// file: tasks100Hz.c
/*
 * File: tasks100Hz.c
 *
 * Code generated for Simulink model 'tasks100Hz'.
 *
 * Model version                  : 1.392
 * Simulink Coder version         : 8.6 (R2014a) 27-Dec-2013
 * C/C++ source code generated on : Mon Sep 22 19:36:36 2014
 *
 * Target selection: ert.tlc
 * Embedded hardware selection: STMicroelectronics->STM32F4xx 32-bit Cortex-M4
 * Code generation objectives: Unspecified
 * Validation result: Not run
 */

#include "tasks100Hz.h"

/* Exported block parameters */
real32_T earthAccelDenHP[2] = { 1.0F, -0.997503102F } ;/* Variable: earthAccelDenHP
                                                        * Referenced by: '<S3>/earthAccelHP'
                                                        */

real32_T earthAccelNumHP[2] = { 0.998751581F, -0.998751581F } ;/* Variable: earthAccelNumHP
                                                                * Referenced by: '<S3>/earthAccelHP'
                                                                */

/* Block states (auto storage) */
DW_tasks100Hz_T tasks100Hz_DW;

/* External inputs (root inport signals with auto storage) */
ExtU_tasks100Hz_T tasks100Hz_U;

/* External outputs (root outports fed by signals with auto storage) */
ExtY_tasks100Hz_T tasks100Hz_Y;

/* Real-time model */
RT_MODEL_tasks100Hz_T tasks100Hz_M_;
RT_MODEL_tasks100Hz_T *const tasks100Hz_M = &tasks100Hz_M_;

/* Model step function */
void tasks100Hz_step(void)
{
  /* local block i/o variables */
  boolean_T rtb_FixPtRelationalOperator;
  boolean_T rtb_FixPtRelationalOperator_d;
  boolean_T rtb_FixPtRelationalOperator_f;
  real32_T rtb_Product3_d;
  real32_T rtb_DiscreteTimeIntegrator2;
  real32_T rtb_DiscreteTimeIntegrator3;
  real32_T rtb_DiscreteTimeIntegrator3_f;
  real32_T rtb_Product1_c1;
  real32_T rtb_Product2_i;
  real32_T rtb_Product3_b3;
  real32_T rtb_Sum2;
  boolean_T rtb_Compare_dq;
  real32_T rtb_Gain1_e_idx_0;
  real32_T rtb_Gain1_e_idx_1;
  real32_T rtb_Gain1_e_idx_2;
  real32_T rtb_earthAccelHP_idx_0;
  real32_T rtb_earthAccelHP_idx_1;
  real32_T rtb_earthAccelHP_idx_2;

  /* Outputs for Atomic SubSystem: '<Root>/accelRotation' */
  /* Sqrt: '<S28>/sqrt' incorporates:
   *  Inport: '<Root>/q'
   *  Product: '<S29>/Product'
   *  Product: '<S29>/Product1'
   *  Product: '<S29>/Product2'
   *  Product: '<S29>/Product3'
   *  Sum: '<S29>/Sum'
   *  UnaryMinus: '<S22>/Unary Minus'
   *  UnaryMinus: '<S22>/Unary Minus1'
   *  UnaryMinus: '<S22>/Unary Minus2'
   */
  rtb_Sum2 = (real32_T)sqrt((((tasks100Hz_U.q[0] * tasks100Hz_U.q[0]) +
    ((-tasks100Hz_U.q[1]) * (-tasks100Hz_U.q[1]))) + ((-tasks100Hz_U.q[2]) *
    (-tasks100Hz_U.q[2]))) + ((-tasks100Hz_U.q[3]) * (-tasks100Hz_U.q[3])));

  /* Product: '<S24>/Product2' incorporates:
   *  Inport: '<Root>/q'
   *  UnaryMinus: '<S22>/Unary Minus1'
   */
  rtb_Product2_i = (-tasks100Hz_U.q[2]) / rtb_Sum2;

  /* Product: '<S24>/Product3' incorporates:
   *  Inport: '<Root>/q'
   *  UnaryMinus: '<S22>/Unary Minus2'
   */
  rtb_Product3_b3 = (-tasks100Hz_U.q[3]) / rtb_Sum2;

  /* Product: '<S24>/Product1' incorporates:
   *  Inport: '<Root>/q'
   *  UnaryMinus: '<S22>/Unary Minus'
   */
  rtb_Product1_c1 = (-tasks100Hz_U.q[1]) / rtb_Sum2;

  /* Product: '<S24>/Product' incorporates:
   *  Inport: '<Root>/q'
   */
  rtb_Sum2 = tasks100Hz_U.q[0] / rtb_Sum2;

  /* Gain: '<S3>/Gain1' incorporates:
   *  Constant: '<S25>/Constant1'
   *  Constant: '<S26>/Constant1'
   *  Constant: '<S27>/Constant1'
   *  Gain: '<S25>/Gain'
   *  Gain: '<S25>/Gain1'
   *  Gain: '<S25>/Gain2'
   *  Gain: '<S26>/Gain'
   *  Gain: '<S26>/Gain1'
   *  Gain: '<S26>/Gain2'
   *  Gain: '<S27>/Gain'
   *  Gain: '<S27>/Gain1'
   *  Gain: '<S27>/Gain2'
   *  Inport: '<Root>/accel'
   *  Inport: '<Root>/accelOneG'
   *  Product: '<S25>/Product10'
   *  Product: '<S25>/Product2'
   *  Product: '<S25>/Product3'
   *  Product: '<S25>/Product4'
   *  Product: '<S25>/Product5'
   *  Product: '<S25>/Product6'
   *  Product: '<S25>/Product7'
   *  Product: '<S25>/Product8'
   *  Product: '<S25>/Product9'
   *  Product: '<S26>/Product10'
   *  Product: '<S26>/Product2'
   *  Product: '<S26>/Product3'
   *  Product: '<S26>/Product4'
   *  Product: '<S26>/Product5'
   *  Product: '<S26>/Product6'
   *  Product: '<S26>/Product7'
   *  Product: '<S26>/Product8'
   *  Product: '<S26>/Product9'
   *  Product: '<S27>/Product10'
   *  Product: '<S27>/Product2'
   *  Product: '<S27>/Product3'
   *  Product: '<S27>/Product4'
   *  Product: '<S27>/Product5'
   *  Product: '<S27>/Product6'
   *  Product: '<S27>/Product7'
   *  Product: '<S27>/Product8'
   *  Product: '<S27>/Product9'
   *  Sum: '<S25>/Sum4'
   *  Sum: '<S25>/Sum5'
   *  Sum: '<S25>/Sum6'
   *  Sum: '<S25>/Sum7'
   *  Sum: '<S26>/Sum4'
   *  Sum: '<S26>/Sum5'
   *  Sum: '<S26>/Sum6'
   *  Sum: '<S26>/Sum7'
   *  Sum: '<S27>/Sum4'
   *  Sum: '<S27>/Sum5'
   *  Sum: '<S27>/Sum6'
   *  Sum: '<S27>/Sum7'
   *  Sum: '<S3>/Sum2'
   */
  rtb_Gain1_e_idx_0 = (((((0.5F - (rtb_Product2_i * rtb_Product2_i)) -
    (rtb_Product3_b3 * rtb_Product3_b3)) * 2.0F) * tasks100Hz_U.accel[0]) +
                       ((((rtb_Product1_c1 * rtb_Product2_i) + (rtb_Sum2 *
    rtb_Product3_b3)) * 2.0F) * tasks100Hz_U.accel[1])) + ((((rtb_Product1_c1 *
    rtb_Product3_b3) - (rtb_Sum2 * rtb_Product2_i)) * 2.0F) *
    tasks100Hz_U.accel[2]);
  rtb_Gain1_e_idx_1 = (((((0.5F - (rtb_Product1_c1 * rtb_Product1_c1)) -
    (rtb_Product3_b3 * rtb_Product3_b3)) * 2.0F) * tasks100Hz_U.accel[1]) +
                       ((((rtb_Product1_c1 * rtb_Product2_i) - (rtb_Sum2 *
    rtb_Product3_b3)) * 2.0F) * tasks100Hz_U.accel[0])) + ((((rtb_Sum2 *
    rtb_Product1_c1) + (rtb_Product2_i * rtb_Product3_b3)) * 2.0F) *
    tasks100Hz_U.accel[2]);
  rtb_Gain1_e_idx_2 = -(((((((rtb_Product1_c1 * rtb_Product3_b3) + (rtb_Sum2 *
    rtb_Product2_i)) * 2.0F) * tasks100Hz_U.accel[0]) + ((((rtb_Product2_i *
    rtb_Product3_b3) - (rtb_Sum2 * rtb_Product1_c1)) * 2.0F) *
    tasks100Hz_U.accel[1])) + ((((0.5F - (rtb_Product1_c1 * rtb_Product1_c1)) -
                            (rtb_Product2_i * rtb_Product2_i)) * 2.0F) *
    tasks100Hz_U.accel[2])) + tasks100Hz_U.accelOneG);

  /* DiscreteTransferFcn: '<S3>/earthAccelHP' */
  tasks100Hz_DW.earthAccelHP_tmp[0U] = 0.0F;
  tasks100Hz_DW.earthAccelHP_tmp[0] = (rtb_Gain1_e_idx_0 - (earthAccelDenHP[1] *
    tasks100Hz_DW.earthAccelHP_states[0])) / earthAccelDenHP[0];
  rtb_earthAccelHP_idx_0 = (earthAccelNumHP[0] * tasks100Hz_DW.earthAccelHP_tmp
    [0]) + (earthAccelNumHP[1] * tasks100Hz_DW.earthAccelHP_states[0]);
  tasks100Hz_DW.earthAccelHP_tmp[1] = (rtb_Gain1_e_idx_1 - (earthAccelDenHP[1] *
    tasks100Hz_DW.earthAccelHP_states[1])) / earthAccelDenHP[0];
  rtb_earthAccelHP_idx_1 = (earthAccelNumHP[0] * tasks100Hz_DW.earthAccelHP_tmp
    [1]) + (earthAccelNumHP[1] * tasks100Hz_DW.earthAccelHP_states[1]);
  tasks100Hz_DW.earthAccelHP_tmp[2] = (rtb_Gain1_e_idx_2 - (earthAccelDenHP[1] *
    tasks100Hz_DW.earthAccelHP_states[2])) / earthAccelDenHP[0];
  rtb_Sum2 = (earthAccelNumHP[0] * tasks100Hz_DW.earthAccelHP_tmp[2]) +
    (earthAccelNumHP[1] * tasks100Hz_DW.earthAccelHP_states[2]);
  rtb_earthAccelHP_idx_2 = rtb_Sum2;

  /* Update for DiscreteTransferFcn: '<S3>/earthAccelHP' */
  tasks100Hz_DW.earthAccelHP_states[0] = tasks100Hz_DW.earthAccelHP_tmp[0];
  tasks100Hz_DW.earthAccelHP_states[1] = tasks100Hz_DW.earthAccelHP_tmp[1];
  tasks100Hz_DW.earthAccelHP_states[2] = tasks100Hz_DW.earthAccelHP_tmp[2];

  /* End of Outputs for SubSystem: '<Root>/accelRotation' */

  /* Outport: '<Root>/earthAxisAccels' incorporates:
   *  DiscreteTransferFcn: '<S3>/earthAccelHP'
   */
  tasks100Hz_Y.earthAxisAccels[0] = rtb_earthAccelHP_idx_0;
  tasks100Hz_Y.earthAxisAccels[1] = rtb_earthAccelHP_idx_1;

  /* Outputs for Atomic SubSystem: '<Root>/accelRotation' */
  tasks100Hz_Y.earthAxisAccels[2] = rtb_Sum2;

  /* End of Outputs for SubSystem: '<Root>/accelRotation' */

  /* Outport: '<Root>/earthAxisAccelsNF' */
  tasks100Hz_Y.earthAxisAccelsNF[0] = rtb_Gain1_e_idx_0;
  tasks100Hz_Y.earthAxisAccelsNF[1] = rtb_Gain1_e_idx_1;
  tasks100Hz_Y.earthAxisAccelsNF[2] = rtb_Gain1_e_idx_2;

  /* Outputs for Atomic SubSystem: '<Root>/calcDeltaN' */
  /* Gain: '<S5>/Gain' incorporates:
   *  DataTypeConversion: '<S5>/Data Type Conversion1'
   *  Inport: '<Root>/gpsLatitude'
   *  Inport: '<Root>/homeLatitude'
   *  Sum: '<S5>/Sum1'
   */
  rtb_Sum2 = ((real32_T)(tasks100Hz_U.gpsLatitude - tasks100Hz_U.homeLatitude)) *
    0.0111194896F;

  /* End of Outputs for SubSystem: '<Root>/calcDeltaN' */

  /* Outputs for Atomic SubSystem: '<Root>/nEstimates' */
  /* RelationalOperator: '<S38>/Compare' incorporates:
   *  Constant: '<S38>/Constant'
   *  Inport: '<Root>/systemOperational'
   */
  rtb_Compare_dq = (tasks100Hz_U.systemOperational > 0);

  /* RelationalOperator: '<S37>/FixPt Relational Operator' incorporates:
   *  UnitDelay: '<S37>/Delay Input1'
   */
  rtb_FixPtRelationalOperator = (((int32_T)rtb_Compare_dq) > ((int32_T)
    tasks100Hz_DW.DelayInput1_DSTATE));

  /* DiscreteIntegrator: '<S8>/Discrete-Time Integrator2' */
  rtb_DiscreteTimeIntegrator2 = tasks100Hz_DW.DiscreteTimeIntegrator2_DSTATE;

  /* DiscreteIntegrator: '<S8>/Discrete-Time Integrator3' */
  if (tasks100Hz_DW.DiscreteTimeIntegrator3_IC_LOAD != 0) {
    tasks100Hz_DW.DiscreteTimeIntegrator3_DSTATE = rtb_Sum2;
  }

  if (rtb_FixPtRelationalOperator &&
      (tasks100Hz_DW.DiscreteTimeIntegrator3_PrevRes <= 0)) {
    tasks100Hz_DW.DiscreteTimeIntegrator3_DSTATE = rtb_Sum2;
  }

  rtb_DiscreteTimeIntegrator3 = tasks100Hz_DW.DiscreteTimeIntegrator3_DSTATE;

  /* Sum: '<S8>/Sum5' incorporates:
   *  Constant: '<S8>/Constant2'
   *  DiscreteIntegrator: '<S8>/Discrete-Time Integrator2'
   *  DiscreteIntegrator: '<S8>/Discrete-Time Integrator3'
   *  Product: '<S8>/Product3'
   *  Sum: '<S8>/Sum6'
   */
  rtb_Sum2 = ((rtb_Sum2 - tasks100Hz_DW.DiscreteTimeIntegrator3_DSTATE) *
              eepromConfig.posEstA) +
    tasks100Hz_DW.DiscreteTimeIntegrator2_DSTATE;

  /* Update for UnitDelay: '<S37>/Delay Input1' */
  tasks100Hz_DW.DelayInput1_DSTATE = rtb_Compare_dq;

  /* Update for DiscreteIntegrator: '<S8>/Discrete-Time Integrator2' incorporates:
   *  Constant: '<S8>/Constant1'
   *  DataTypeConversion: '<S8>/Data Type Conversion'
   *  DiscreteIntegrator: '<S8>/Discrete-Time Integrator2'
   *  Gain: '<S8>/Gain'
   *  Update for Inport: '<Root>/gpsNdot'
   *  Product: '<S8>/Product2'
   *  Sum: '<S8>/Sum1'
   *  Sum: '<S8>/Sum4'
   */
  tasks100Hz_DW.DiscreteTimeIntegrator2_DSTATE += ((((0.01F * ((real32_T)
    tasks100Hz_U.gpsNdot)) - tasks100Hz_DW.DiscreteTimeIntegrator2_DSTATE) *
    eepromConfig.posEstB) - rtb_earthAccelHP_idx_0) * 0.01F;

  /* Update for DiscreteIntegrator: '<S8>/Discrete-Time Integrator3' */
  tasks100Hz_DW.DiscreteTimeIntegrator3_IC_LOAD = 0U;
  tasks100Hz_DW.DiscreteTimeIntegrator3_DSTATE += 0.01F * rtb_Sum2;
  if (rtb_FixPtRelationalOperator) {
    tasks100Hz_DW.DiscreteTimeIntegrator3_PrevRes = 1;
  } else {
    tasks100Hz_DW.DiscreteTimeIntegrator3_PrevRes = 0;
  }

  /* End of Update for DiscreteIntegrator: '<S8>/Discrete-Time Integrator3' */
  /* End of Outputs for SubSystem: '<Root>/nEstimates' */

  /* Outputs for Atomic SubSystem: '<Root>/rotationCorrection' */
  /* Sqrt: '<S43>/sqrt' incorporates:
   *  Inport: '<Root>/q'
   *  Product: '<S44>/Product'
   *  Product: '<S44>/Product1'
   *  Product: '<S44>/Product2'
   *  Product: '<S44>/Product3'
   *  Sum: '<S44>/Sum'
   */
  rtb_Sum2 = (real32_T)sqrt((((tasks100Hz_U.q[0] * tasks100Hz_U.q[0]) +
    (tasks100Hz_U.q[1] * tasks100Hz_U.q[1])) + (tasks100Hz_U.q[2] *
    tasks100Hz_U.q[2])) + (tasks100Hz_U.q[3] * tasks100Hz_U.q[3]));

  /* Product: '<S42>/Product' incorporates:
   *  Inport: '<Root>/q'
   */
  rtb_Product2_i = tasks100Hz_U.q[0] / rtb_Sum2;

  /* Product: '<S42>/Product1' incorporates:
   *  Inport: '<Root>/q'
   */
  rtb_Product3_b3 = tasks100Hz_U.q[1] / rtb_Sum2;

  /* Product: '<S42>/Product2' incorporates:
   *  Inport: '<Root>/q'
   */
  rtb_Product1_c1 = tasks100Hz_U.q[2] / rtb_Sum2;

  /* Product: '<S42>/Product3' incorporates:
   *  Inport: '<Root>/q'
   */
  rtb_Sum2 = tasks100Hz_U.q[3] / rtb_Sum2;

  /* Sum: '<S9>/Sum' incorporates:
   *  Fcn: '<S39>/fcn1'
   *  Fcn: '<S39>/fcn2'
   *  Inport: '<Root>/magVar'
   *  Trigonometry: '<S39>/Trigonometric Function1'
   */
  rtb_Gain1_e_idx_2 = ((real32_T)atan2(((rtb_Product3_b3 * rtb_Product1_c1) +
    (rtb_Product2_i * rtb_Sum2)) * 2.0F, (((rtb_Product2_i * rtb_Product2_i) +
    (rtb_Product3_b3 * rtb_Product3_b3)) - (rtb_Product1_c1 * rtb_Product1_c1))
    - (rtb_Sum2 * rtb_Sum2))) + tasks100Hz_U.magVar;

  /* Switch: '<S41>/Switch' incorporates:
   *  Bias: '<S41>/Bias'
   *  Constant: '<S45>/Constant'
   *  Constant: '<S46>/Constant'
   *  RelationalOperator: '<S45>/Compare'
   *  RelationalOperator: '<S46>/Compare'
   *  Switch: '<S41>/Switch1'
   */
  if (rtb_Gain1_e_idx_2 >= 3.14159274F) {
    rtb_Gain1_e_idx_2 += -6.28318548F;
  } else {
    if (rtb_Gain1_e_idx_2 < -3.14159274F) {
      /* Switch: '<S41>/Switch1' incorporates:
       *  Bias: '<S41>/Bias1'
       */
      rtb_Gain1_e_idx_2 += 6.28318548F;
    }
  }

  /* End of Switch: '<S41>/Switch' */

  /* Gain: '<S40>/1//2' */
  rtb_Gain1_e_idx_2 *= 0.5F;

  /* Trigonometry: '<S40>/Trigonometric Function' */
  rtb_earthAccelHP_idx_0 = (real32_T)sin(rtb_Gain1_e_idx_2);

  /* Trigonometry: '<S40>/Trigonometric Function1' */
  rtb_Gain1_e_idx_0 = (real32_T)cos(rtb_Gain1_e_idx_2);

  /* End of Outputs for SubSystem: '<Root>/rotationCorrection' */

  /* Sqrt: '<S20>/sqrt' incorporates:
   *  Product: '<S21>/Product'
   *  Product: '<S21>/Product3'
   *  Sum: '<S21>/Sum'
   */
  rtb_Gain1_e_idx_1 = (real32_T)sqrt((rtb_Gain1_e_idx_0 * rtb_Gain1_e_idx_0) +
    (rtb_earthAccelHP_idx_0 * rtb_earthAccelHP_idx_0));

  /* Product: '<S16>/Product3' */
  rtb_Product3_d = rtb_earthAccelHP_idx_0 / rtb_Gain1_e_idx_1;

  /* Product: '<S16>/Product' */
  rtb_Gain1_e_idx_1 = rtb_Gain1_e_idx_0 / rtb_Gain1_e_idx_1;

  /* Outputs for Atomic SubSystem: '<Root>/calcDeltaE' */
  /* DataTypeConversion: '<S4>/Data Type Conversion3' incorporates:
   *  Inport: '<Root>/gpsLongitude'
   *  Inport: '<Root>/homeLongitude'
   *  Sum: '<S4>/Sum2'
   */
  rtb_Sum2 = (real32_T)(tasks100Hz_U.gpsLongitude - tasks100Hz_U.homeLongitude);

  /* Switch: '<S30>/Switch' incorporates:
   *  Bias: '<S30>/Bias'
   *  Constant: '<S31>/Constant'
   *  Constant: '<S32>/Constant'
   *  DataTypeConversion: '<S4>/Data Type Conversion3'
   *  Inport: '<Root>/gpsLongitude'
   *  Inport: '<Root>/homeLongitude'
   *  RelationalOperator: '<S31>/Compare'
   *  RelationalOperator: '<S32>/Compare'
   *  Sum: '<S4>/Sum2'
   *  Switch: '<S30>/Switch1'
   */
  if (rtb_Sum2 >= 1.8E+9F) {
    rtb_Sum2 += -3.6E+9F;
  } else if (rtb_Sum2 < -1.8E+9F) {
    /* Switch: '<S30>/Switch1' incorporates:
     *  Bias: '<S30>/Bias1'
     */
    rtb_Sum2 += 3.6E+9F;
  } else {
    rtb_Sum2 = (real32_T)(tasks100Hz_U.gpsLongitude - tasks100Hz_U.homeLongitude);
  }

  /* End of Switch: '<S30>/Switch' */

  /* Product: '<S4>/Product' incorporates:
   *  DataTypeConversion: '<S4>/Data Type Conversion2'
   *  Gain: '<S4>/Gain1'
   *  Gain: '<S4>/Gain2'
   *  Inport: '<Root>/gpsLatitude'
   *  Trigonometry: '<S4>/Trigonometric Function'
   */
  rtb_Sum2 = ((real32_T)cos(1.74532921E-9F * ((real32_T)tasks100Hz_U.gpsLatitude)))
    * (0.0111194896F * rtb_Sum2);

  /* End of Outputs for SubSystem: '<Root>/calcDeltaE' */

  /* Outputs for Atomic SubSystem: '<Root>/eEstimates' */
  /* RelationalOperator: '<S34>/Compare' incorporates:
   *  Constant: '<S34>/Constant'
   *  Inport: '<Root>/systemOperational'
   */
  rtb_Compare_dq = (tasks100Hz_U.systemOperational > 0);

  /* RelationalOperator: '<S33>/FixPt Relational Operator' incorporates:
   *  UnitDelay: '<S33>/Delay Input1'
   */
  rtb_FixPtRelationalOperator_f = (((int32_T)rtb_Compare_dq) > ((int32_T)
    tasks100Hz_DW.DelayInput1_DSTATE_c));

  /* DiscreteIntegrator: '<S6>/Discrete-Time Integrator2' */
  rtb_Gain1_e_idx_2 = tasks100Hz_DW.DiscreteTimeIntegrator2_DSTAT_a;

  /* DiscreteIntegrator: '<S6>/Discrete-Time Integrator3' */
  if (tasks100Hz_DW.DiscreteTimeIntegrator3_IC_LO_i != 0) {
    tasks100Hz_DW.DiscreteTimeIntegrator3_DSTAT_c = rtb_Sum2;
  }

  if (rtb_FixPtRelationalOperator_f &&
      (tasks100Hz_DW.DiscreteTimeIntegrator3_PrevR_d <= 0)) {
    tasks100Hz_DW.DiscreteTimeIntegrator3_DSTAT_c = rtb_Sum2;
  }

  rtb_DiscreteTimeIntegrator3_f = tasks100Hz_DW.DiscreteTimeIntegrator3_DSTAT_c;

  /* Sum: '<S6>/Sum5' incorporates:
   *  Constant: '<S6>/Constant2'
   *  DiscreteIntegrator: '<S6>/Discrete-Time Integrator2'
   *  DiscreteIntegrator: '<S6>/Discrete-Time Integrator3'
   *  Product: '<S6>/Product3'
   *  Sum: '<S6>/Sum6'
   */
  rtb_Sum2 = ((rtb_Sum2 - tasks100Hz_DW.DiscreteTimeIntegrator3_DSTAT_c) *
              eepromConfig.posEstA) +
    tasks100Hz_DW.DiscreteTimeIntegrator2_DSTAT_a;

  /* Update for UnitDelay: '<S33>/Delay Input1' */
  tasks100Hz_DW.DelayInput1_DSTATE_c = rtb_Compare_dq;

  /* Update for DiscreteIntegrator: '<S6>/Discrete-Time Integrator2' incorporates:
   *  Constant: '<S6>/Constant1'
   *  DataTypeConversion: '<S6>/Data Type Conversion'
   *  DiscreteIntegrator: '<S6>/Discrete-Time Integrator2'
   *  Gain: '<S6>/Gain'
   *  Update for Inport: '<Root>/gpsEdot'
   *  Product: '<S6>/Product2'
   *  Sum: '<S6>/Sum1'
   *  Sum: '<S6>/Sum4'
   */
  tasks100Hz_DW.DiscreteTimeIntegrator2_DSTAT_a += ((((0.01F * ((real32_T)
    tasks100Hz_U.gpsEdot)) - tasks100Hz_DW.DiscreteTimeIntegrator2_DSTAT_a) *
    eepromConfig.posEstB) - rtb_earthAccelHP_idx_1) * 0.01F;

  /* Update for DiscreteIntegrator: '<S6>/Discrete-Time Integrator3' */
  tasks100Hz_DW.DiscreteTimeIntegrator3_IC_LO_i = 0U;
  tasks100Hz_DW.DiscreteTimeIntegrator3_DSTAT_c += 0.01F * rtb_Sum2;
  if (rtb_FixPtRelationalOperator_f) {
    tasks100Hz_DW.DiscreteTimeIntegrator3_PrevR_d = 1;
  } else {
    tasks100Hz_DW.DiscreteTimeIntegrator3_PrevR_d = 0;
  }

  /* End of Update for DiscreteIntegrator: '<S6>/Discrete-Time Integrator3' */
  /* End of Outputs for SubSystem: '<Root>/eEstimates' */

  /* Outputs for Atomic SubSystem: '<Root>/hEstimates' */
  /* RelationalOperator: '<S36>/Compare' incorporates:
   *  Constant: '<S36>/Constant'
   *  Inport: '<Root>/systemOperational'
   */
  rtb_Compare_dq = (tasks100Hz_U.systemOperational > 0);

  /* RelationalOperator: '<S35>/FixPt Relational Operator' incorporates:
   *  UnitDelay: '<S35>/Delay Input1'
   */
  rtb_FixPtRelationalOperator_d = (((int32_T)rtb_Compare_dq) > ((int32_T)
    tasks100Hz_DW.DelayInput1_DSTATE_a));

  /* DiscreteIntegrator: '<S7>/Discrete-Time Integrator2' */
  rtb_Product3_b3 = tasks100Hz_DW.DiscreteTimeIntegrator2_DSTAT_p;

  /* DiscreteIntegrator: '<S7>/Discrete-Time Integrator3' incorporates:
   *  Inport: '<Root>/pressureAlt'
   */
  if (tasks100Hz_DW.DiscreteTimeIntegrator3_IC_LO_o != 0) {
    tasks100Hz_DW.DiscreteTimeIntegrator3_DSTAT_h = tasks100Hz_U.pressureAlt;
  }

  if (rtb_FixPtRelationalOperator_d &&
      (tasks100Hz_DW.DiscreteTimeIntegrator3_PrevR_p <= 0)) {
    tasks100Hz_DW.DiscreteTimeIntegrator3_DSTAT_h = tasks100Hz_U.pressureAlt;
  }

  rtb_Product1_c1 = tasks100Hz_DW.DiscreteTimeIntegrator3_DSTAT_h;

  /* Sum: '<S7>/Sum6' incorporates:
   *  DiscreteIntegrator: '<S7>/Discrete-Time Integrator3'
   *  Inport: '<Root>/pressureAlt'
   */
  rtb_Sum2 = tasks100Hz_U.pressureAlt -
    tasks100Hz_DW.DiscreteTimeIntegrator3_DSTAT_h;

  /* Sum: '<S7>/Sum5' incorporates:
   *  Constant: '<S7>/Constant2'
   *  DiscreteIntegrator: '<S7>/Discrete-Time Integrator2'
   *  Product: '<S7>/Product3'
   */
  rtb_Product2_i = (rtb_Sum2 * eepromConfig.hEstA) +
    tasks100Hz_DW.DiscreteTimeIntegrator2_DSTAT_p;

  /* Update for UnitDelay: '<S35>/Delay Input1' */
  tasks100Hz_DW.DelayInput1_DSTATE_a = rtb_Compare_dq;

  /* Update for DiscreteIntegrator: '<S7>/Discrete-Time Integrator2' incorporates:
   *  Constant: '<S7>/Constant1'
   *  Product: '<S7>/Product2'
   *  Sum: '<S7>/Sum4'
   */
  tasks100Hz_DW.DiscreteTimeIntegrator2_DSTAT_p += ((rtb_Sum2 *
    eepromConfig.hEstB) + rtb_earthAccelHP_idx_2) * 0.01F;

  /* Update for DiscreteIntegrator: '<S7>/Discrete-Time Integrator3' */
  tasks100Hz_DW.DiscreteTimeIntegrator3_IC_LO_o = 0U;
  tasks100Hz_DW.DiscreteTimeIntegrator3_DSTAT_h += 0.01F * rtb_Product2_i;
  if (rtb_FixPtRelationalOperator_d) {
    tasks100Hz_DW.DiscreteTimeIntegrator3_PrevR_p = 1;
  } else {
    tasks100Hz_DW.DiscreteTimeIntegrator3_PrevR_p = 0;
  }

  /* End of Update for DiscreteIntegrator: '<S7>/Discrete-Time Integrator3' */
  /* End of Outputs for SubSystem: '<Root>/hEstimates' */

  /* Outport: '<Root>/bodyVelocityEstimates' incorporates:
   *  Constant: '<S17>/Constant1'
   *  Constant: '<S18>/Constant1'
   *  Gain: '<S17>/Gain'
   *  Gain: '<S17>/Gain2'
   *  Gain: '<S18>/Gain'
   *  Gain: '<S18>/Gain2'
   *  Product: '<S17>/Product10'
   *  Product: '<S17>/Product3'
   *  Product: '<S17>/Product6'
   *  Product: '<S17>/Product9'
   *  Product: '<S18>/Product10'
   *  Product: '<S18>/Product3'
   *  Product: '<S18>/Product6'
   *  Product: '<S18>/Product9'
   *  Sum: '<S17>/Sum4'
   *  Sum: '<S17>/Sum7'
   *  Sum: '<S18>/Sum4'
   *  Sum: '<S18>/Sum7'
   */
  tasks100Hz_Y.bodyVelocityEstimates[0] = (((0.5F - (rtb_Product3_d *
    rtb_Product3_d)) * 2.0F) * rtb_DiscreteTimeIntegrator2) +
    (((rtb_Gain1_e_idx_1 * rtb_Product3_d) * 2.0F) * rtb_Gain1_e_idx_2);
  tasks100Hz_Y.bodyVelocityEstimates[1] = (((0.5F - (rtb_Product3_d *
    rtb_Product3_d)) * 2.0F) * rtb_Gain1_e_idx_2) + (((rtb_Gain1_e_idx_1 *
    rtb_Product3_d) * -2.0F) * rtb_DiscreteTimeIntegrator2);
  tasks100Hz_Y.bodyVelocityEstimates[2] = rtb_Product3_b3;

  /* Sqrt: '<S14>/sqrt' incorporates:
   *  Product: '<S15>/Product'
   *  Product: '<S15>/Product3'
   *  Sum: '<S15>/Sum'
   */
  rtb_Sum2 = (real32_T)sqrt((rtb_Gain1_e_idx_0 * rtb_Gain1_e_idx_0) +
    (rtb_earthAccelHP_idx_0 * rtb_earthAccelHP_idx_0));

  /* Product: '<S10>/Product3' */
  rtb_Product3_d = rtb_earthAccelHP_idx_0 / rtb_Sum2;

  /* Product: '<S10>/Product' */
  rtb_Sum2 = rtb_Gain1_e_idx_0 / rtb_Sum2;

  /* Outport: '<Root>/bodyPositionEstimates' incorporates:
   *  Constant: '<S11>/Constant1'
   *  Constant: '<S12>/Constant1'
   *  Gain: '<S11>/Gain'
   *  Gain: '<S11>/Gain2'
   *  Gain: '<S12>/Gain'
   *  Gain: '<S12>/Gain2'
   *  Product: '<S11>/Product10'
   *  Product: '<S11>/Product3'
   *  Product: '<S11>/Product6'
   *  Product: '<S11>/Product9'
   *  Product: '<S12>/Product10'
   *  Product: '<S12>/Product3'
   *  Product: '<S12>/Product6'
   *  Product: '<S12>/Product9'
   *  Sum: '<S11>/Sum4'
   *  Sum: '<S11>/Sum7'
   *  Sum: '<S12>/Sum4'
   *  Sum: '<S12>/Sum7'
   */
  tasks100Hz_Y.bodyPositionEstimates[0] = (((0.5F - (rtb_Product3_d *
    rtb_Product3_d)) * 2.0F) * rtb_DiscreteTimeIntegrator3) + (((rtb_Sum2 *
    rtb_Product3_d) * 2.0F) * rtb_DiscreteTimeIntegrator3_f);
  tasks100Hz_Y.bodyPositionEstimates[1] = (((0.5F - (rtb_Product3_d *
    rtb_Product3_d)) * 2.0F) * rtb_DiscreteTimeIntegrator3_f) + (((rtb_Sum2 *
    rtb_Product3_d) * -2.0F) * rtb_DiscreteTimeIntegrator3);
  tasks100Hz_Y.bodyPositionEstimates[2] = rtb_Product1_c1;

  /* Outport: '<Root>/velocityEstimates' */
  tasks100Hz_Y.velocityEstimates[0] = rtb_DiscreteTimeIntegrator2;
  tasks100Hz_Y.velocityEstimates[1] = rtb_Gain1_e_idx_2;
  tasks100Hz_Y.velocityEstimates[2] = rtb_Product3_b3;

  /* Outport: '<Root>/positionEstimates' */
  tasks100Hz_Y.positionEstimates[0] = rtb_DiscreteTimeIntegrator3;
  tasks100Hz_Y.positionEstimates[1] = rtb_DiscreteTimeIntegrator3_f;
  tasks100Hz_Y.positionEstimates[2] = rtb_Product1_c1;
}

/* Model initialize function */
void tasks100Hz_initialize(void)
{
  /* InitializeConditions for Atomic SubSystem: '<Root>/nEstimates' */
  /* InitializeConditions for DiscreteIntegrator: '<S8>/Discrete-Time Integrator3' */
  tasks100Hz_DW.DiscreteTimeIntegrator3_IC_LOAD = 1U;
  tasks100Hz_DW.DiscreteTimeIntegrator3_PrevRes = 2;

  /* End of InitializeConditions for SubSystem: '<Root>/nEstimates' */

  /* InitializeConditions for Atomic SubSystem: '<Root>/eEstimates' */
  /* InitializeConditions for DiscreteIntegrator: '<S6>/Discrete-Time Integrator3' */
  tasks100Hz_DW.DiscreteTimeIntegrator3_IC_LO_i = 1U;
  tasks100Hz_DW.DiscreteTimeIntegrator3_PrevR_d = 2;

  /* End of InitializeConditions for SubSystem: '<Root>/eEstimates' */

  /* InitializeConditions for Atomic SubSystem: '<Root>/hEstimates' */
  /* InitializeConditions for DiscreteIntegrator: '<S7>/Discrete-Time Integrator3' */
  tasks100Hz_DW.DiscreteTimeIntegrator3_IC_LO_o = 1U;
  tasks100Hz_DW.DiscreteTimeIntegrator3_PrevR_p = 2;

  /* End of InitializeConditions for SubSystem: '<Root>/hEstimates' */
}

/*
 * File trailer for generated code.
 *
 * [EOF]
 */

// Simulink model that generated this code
simulink model "tasks100Hz"  (R2014a)
settings: Solver=FixedStepDiscrete  StartTime=0.0  StopTime=simTime  FixedStep=filterDT  RelTol=1e-3
values from neighbouring files (symbols this model uses):
  earthAccelDenHP = p    [setup.m]
  earthAccelNumHP = p    [setup.m]
  eepromConfig = p    [setup.m]
  filterDT = 1 / 100    (= 0.01)    [setup.m]
undefined symbols (not defined in the file or in its folder): DiscIntNeverNeededParam
libraries: simulink x7, aerolibutil x4, aerolibtransform2 x1

== system tasks100Hz ==
  q : Inport  OutDataTypeStr=single  PortDimensions=4  SampleTime=filterDT
  accel : Inport  Port=2  OutDataTypeStr=single  PortDimensions=3  SampleTime=filterDT
  accelOneG : Inport  Port=3  OutDataTypeStr=single  PortDimensions=1  SampleTime=filterDT
  gpsLatitude : Inport  Port=4  OutDataTypeStr=int32  PortDimensions=1  SampleTime=filterDT
  homeLatitude : Inport  Port=5  OutDataTypeStr=int32  PortDimensions=1  SampleTime=filterDT
  gpsNdot : Inport  Port=6  OutDataTypeStr=int32  PortDimensions=1  SampleTime=filterDT
  gpsLongitude : Inport  Port=7  OutDataTypeStr=int32  PortDimensions=1  SampleTime=filterDT
  homeLongitude : Inport  Port=8  OutDataTypeStr=int32  PortDimensions=1  SampleTime=filterDT
  gpsEdot : Inport  Port=9  OutDataTypeStr=int32  PortDimensions=1  SampleTime=filterDT
  pressureAlt : Inport  Port=10  OutDataTypeStr=single  PortDimensions=1  SampleTime=filterDT
  systemOperational : Inport  Port=11  OutDataTypeStr=uint8  PortDimensions=1  SampleTime=filterDT
  magVar : Inport  Port=12  OutDataTypeStr=single  PortDimensions=1  SampleTime=filterDT
  Data Type Conversion4 : DataTypeConversion  OutDataTypeStr=single
  Data Type Conversion5 : DataTypeConversion  OutDataTypeStr=single
  Mux : Mux  Inputs=3
  Mux2 : Mux  Inputs=3
  Quaternion Rotation1 : Subsystem
  Quaternion Rotation2 : Subsystem
  accelRotation : Subsystem  TreatAsAtomicUnit=on
  calcDeltaE : Subsystem  TreatAsAtomicUnit=on
  calcDeltaN : Subsystem  TreatAsAtomicUnit=on
  eEstimates : Subsystem  TreatAsAtomicUnit=on
  hEstimates : Subsystem  TreatAsAtomicUnit=on
  nEstimates : Subsystem  TreatAsAtomicUnit=on
  rotationCorrection : Subsystem  TreatAsAtomicUnit=on
  earthAxisAccels : Outport  OutDataTypeStr=single  PortDimensions=3  SampleTime=filterDT
  earthAxisAccelsNF : Outport  Port=2  OutDataTypeStr=single  PortDimensions=3  SampleTime=filterDT
  bodyVelocityEstimates : Outport  Port=3  OutDataTypeStr=single  PortDimensions=3  SampleTime=filterDT
  bodyPositionEstimates : Outport  Port=4  OutDataTypeStr=single  PortDimensions=3  SampleTime=filterDT
  velocityEstimates : Outport  Port=5  OutDataTypeStr=single  PortDimensions=3  SampleTime=filterDT
  positionEstimates : Outport  Port=6  OutDataTypeStr=single  PortDimensions=3  SampleTime=filterDT
  wires:
  systemOperational/1 -> nEstimates/2(systemOperational), eEstimates/2(systemOperational), hEstimates/2(systemOperational)
  pressureAlt/1 -> hEstimates/3(pressureAlt)
  hEstimates/1(hDotEstimate) -> Mux/3
  gpsNdot/1 -> nEstimates/4(nDotGPS)
  gpsEdot/1 -> eEstimates/4(eDotGPS)
  nEstimates/1(nDotEstimate) -> Mux/1
  nEstimates/2(nEstimate) -> Mux2/1
  eEstimates/1(eDotEstimate) -> Mux/2
  eEstimates/2(eEstimate) -> Mux2/2
  Quaternion Rotation2/1(vec_rot) -> Data Type Conversion4/1
  Quaternion Rotation1/1(vec_rot) -> Data Type Conversion5/1
  Data Type Conversion4/1 -> bodyVelocityEstimates/1
  Data Type Conversion5/1 -> bodyPositionEstimates/1
  hEstimates/2(hEstimate) -> Mux2/3
  Mux2/1 -> positionEstimates/1, Quaternion Rotation1/2(vec)
  accelOneG/1 -> accelRotation/3(accelOneG)
  homeLatitude/1 -> calcDeltaN/2(homeLatitude)
  calcDeltaN/1(deltaN) -> nEstimates/3(deltaN)
  gpsLongitude/1 -> calcDeltaE/2(gpsLongitude)
  homeLongitude/1 -> calcDeltaE/3(homeLongitude)
  calcDeltaE/1(deltaE) -> eEstimates/3(deltaE)
  gpsLatitude/1 -> calcDeltaN/1(gpsLatitude), calcDeltaE/1(gpsLatitude)
  q/1 -> rotationCorrection/2(qIn), accelRotation/1(q)
  accelRotation/2(earthAxisAccelsNF) -> earthAxisAccelsNF/1
  accelRotation/1(earthAxisAccels) -> eEstimates/1(earthAxisAccels), hEstimates/1(earthAxisAccels), nEstimates/1(earthAxisAccels), earthAxisAccels/1
  accel/1 -> accelRotation/2(accel)
  Mux/1 -> velocityEstimates/1, Quaternion Rotation2/2(vec)
  magVar/1 -> rotationCorrection/1(magVar)
  rotationCorrection/1(qOut) -> Quaternion Rotation2/1(q), Quaternion Rotation1/1(q)

== system tasks100Hz/Quaternion Rotation1 ==
  q : Inport
  vec : Inport  Port=2
  Mux1 : Mux  Inputs=3
  Quaternion Normalize : aerolibutil/Quaternion Normalize
  singleV1 : Subsystem
  singleV2 : Subsystem
  singleV3 : Subsystem
  vec_rot : Outport
  wires:
  q/1 -> Quaternion Normalize/1
  singleV1/1(V1) -> Mux1/1
  vec/1 -> singleV1/2(vec), singleV3/2(vec), singleV2/2(vec)
  Quaternion Normalize/1 -> singleV1/1(q), singleV3/1(q), singleV2/1(q)
  Mux1/1 -> vec_rot/1
  singleV3/1(V3) -> Mux1/3
  singleV2/1(V2) -> Mux1/2

== system tasks100Hz/Quaternion Rotation2 ==
  q : Inport
  vec : Inport  Port=2
  Mux1 : Mux  Inputs=3
  Quaternion Normalize : aerolibutil/Quaternion Normalize
  singleV1 : Subsystem
  singleV2 : Subsystem
  singleV3 : Subsystem
  vec_rot : Outport
  wires:
  singleV2/1(V2) -> Mux1/2
  singleV3/1(V3) -> Mux1/3
  Mux1/1 -> vec_rot/1
  Quaternion Normalize/1 -> singleV2/1(q), singleV3/1(q), singleV1/1(q)
  vec/1 -> singleV2/2(vec), singleV3/2(vec), singleV1/2(vec)
  singleV1/1(V1) -> Mux1/1
  q/1 -> Quaternion Normalize/1

== system tasks100Hz/accelRotation ==
  q : Inport
  accel : Inport  Port=2
  accelOneG : Inport  Port=3
  Demux1 : Demux  Outputs=[2 1]
  Gain1 : Gain  Gain=[1 1 -1]
  Mux1 : Mux  Inputs=[2 1]
  Quaternion Conjugate : aerolibutil/Quaternion Conjugate
  Quaternion Rotation : Subsystem
  Sum2 : Sum  Inputs=|++
  earthAccelHP : DiscreteTransferFcn  Numerator=earthAccelNumHP  Denominator=earthAccelDenHP
  earthAxisAccels : Outport
  earthAxisAccelsNF : Outport  Port=2
  wires:
  Gain1/1 -> earthAxisAccelsNF/1, earthAccelHP/1
  accelOneG/1 -> Sum2/2
  Demux1/1 -> Mux1/1
  Sum2/1 -> Mux1/2
  Demux1/2 -> Sum2/1
  Quaternion Conjugate/1 -> Quaternion Rotation/1(q)
  accel/1 -> Quaternion Rotation/2(vec)
  q/1 -> Quaternion Conjugate/1
  Quaternion Rotation/1(vec_rot) -> Demux1/1
  Mux1/1 -> Gain1/1
  earthAccelHP/1 -> earthAxisAccels/1

== system tasks100Hz/calcDeltaE ==
  gpsLatitude : Inport
  gpsLongitude : Inport  Port=2
  homeLongitude : Inport  Port=3
  Data Type Conversion2 : DataTypeConversion  OutDataTypeStr=single
  Data Type Conversion3 : DataTypeConversion  OutDataTypeStr=single
  Gain1 : Gain  Gain=pi / 180 * 1e-7
  Gain2 : Gain  Gain=0.01111949
  Product : Product
  Sum2 : Sum  Inputs=|+-
  Trigonometric Function : Trigonometry  Operator=cos
  stdRadianLimit : Subsystem
  deltaE : Outport
  wires:
  stdRadianLimit/1(stdDegrees) -> Gain2/1
  gpsLatitude/1 -> Data Type Conversion2/1
  Data Type Conversion3/1 -> stdRadianLimit/1(degrees)
  Product/1 -> deltaE/1
  Sum2/1 -> Data Type Conversion3/1
  homeLongitude/1 -> Sum2/2
  Gain2/1 -> Product/2
  Trigonometric Function/1 -> Product/1
  Gain1/1 -> Trigonometric Function/1
  Data Type Conversion2/1 -> Gain1/1
  gpsLongitude/1 -> Sum2/1

== system tasks100Hz/calcDeltaN ==
  gpsLatitude : Inport
  homeLatitude : Inport  Port=2
  Data Type Conversion1 : DataTypeConversion  OutDataTypeStr=single
  Gain : Gain  Gain=0.01111949
  Sum1 : Sum  Inputs=|+-
  deltaN : Outport
  wires:
  Sum1/1 -> Data Type Conversion1/1
  homeLatitude/1 -> Sum1/2
  Data Type Conversion1/1 -> Gain/1
  gpsLatitude/1 -> Sum1/1
  Gain/1 -> deltaN/1

== system tasks100Hz/eEstimates ==
  earthAxisAccels : Inport
  systemOperational : Inport  Port=2
  deltaE : Inport  Port=3
  eDotGPS : Inport  Port=4  OutDataTypeStr=int32
  Constant1 : Constant  Value=eepromConfig.posEstB  SampleTime=filterDT
  Constant2 : Constant  Value=eepromConfig.posEstA  SampleTime=filterDT
  Data Type Conversion : DataTypeConversion  OutDataTypeStr=single
  Detect Rise Positive1 : simulink/Logic and Bit Operations/Detect Rise Positive  vinit=0  InputProcessing=Inherited  OutDataTypeStr=boolean
  Discrete-Time Integrator2 : DiscreteIntegrator  SampleTime=filterDT  ICPrevOutput=DiscIntNeverNeededParam  ICPrevScaledInput=DiscIntNeverNeededParam
  Discrete-Time Integrator3 : DiscreteIntegrator  ExternalReset=rising  InitialConditionSource=external  SampleTime=filterDT  ICPrevOutput=DiscIntNeverNeededParam  ICPrevScaledInput=DiscIntNeverNeededParam
  Gain : Gain  Gain=0.01
  Product2 : Product
  Product3 : Product
  Selector1 : Selector  IndexMode=Zero-based  InputPortWidth=3
  Sum1 : Sum  Inputs=+-|
  Sum4 : Sum  Inputs=+-|
  Sum5 : Sum  Inputs=|++
  Sum6 : Sum  Inputs=-+|
  eDotEstimate : Outport
  eEstimate : Outport  Port=2
  wires:
  Data Type Conversion/1 -> Gain/1
  Gain/1 -> Sum1/1
  eDotGPS/1 -> Data Type Conversion/1
  Sum1/1 -> Product2/2
  Constant1/1 -> Product2/1
  Product2/1 -> Sum4/1
  Selector1/1 -> Sum4/2
  Sum4/1 -> Discrete-Time Integrator2/1
  Product3/1 -> Sum5/2
  Detect Rise Positive1/1 -> Discrete-Time Integrator3/2
  Constant2/1 -> Product3/2
  Discrete-Time Integrator3/1 -> eEstimate/1, Sum6/1
  Sum6/1 -> Product3/1
  Discrete-Time Integrator2/1 -> eDotEstimate/1, Sum1/2, Sum5/1
  Sum5/1 -> Discrete-Time Integrator3/1
  earthAxisAccels/1 -> Selector1/1
  deltaE/1 -> Discrete-Time Integrator3/3, Sum6/2
  systemOperational/1 -> Detect Rise Positive1/1

== system tasks100Hz/hEstimates ==
  earthAxisAccels : Inport
  systemOperational : Inport  Port=2
  pressureAlt : Inport  Port=3
  Constant1 : Constant  Value=eepromConfig.hEstB  SampleTime=filterDT
  Constant2 : Constant  Value=eepromConfig.hEstA  SampleTime=filterDT
  Detect Rise Positive1 : simulink/Logic and Bit Operations/Detect Rise Positive  vinit=0  InputProcessing=Inherited  OutDataTypeStr=boolean
  Discrete-Time Integrator2 : DiscreteIntegrator  SampleTime=filterDT  ICPrevOutput=DiscIntNeverNeededParam  ICPrevScaledInput=DiscIntNeverNeededParam
  Discrete-Time Integrator3 : DiscreteIntegrator  ExternalReset=rising  InitialConditionSource=external  SampleTime=filterDT  ICPrevOutput=DiscIntNeverNeededParam  ICPrevScaledInput=DiscIntNeverNeededParam
  Product2 : Product
  Product3 : Product
  Selector1 : Selector  IndexMode=Zero-based  InputPortWidth=3  Indices=2
  Sum4 : Sum  Inputs=|++
  Sum5 : Sum  Inputs=|++
  Sum6 : Sum  Inputs=-+|
  hDotEstimate : Outport
  hEstimate : Outport  Port=2
  wires:
  systemOperational/1 -> Detect Rise Positive1/1
  pressureAlt/1 -> Sum6/2, Discrete-Time Integrator3/3
  earthAxisAccels/1 -> Selector1/1
  Sum5/1 -> Discrete-Time Integrator3/1
  Discrete-Time Integrator2/1 -> Sum5/1, hDotEstimate/1
  Sum6/1 -> Product3/1, Product2/1
  Discrete-Time Integrator3/1 -> Sum6/1, hEstimate/1
  Constant2/1 -> Product3/2
  Selector1/1 -> Sum4/1
  Detect Rise Positive1/1 -> Discrete-Time Integrator3/2
  Product3/1 -> Sum5/2
  Sum4/1 -> Discrete-Time Integrator2/1
  Constant1/1 -> Product2/2
  Product2/1 -> Sum4/2

== system tasks100Hz/nEstimates ==
  earthAxisAccels : Inport
  systemOperational : Inport  Port=2
  deltaN : Inport  Port=3
  nDotGPS : Inport  Port=4  OutDataTypeStr=int32
  Constant1 : Constant  Value=eepromConfig.posEstB  SampleTime=filterDT
  Constant2 : Constant  Value=eepromConfig.posEstA  SampleTime=filterDT
  Data Type Conversion : DataTypeConversion  OutDataTypeStr=single
  Detect Rise Positive1 : simulink/Logic and Bit Operations/Detect Rise Positive  vinit=0  InputProcessing=Inherited  OutDataTypeStr=boolean
  Discrete-Time Integrator2 : DiscreteIntegrator  SampleTime=filterDT  ICPrevOutput=DiscIntNeverNeededParam  ICPrevScaledInput=DiscIntNeverNeededParam
  Discrete-Time Integrator3 : DiscreteIntegrator  ExternalReset=rising  InitialConditionSource=external  SampleTime=filterDT  ICPrevOutput=DiscIntNeverNeededParam  ICPrevScaledInput=DiscIntNeverNeededParam
  Gain : Gain  Gain=0.01
  Product2 : Product
  Product3 : Product
  Selector1 : Selector  IndexMode=Zero-based  InputPortWidth=3  Indices=0
  Sum1 : Sum  Inputs=+-|
  Sum4 : Sum  Inputs=+-|
  Sum5 : Sum  Inputs=|++
  Sum6 : Sum  Inputs=-+|
  nDotEstimate : Outport
  nEstimate : Outport  Port=2
  wires:
  systemOperational/1 -> Detect Rise Positive1/1
  deltaN/1 -> Sum6/2, Discrete-Time Integrator3/3
  earthAxisAccels/1 -> Selector1/1
  Sum5/1 -> Discrete-Time Integrator3/1
  Discrete-Time Integrator2/1 -> Sum5/1, Sum1/2, nDotEstimate/1
  Sum6/1 -> Product3/1
  Discrete-Time Integrator3/1 -> Sum6/1, nEstimate/1
  Constant2/1 -> Product3/2
  Detect Rise Positive1/1 -> Discrete-Time Integrator3/2
  Product3/1 -> Sum5/2
  Sum4/1 -> Discrete-Time Integrator2/1
  Selector1/1 -> Sum4/2
  Product2/1 -> Sum4/1
  Constant1/1 -> Product2/1
  Sum1/1 -> Product2/2
  nDotGPS/1 -> Data Type Conversion/1
  Gain/1 -> Sum1/1
  Data Type Conversion/1 -> Gain/1

== system tasks100Hz/rotationCorrection ==
  magVar : Inport
  qIn : Inport  Port=2
  Demux : Demux  Outputs=[1 2]
  Gain3 : Gain  Gain=[1 0 0]
  Mux : Mux  Inputs=[1 2]
  Quaternions to Rotation Angles : aerolibtransform2/Quaternions to Rotation Angles  rotationOrder=ZYX
  Rotation Angles to Quaternions Rotation Order: ZYX : Subsystem
  Sum : Sum  Inputs=++|
  stdRadianLimit : Subsystem
  qOut : Outport
  wires:
  Mux/1 -> Rotation Angles to Quaternions Rotation Order: ZYX/1("R1, R2, R3")
  Gain3/1 -> Demux/1
  stdRadianLimit/1(stdRadians) -> Mux/1
  Demux/1 -> Sum/2
  Demux/2 -> Mux/2
  magVar/1 -> Sum/1
  Sum/1 -> stdRadianLimit/1(radians)
  qIn/1 -> Quaternions to Rotation Angles/1
  Quaternions to Rotation Angles/1 -> Gain3/1
  Rotation Angles to Quaternions Rotation Order: ZYX/1(q) -> qOut/1

== system tasks100Hz/Quaternion Rotation1/singleV1 ==
  q : Inport
  vec : Inport  Port=2
  Constant1 : Constant  Value=0.5  OutDataTypeStr=single
  Demux1 : Demux
  Demux2 : Demux  Outputs=3
  Demux4 : Demux
  Gain : Gain  Gain=2
  Gain2 : Gain  Gain=2
  Product{3,6,9..10} (4 alike) : Product  RndMeth=Zero
  Sum4 : Sum  Inputs=++|
  Sum7 : Sum  Inputs=|-+
  Terminator{1..6} (6 alike) : Terminator
  V1 : Outport
  wires:
  Product6/1 -> Sum4/2
  Sum4/1 -> V1/1
  q/1 -> Demux4/1, Demux1/1
  vec/1 -> Demux2/1
  Demux1/4 -> Product3/2
  Demux1/1 -> Product3/1
  Product3/1 -> Gain/1
  Product10/1 -> Sum4/1
  Demux4/2 -> Terminator2/1
  Gain/1 -> Product6/1
  Gain2/1 -> Product10/2
  Demux2/2 -> Product6/2
  Demux2/1 -> Product10/1
  Sum7/1 -> Gain2/1
  Demux4/1 -> Terminator1/1
  Demux4/3 -> Terminator3/1
  Demux4/4 -> Product9/1, Product9/2
  Product9/1 -> Sum7/1
  Constant1/1 -> Sum7/2
  Demux1/3 -> Terminator4/1
  Demux1/2 -> Terminator5/1
  Demux2/3 -> Terminator6/1

== system tasks100Hz/Quaternion Rotation1/singleV2 ==
  q : Inport
  vec : Inport  Port=2
  Constant1 : Constant  Value=0.5  OutDataTypeStr=single
  Demux1 : Demux
  Demux2 : Demux  Outputs=3
  Demux4 : Demux
  Gain : Gain  Gain=-2
  Gain2 : Gain  Gain=2
  Product{3,6,9..10} (4 alike) : Product  RndMeth=Zero
  Sum4 : Sum  Inputs=++|
  Sum7 : Sum  Inputs=|-+
  Terminator{1..6} (6 alike) : Terminator
  V2 : Outport
  wires:
  Demux1/1 -> Product3/1
  Demux1/4 -> Product3/2
  Gain/1 -> Product6/2
  Sum7/1 -> Gain2/1
  Product10/1 -> Sum4/2
  Demux4/1 -> Terminator1/1
  Sum4/1 -> V2/1
  Demux4/4 -> Product9/1, Product9/2
  q/1 -> Demux1/1, Demux4/1
  vec/1 -> Demux2/1
  Demux2/1 -> Product6/1
  Demux2/2 -> Product10/2
  Demux4/3 -> Terminator2/1
  Gain2/1 -> Product10/1
  Product6/1 -> Sum4/1
  Product3/1 -> Gain/1
  Demux1/2 -> Terminator4/1
  Demux1/3 -> Terminator3/1
  Constant1/1 -> Sum7/2
  Product9/1 -> Sum7/1
  Demux4/2 -> Terminator5/1
  Demux2/3 -> Terminator6/1

== system tasks100Hz/Quaternion Rotation1/singleV3 ==
  q : Inport
  vec : Inport  Port=2
  Demux2 : Demux  Outputs=3
  Terminator1 : Terminator
  Terminator2 : Terminator
  Terminator3 : Terminator
  V3 : Outport
  wires:
  vec/1 -> Demux2/1
  Demux2/1 -> Terminator2/1
  Demux2/2 -> Terminator3/1
  Demux2/3 -> V3/1
  q/1 -> Terminator1/1

== system tasks100Hz/Quaternion Rotation2/singleV1 ==
  q : Inport
  vec : Inport  Port=2
  Constant1 : Constant  Value=0.5  OutDataTypeStr=single
  Demux1 : Demux
  Demux2 : Demux  Outputs=3
  Demux4 : Demux
  Gain : Gain  Gain=2
  Gain2 : Gain  Gain=2
  Product{3,6,9..10} (4 alike) : Product  RndMeth=Zero
  Sum4 : Sum  Inputs=++|
  Sum7 : Sum  Inputs=|-+
  Terminator{1..6} (6 alike) : Terminator
  V1 : Outport
  wires:
  Demux2/3 -> Terminator6/1
  Demux1/2 -> Terminator5/1
  Demux1/3 -> Terminator4/1
  Constant1/1 -> Sum7/2
  Product9/1 -> Sum7/1
  Demux4/4 -> Product9/2, Product9/1
  Demux4/3 -> Terminator3/1
  Demux4/1 -> Terminator1/1
  Sum7/1 -> Gain2/1
  Demux2/1 -> Product10/1
  Demux2/2 -> Product6/2
  Gain2/1 -> Product10/2
  Gain/1 -> Product6/1
  Demux4/2 -> Terminator2/1
  Product10/1 -> Sum4/1
  Product3/1 -> Gain/1
  Demux1/1 -> Product3/1
  Demux1/4 -> Product3/2
  vec/1 -> Demux2/1
  q/1 -> Demux1/1, Demux4/1
  Sum4/1 -> V1/1
  Product6/1 -> Sum4/2

== system tasks100Hz/Quaternion Rotation2/singleV2 ==
  q : Inport
  vec : Inport  Port=2
  Constant1 : Constant  Value=0.5  OutDataTypeStr=single
  Demux1 : Demux
  Demux2 : Demux  Outputs=3
  Demux4 : Demux
  Gain : Gain  Gain=-2
  Gain2 : Gain  Gain=2
  Product{3,6,9..10} (4 alike) : Product  RndMeth=Zero
  Sum4 : Sum  Inputs=++|
  Sum7 : Sum  Inputs=|-+
  Terminator{1..6} (6 alike) : Terminator
  V2 : Outport
  wires:
  Demux2/3 -> Terminator6/1
  Demux4/2 -> Terminator5/1
  Product9/1 -> Sum7/1
  Constant1/1 -> Sum7/2
  Demux1/3 -> Terminator3/1
  Demux1/2 -> Terminator4/1
  Product3/1 -> Gain/1
  Product6/1 -> Sum4/1
  Gain2/1 -> Product10/1
  Demux4/3 -> Terminator2/1
  Demux2/2 -> Product10/2
  Demux2/1 -> Product6/1
  vec/1 -> Demux2/1
  q/1 -> Demux4/1, Demux1/1
  Demux4/4 -> Product9/2, Product9/1
  Sum4/1 -> V2/1
  Demux4/1 -> Terminator1/1
  Product10/1 -> Sum4/2
  Sum7/1 -> Gain2/1
  Gain/1 -> Product6/2
  Demux1/4 -> Product3/2
  Demux1/1 -> Product3/1

== system tasks100Hz/Quaternion Rotation2/singleV3 ==
  q : Inport
  vec : Inport  Port=2
  Demux2 : Demux  Outputs=3
  Terminator1 : Terminator
  Terminator2 : Terminator
  Terminator3 : Terminator
  V3 : Outport
  wires:
  q/1 -> Terminator1/1
  Demux2/3 -> V3/1
  Demux2/2 -> Terminator3/1
  Demux2/1 -> Terminator2/1
  vec/1 -> Demux2/1

== system tasks100Hz/accelRotation/Quaternion Rotation ==
  q : Inport
  vec : Inport  Port=2
  Mux1 : Mux  Inputs=3
  Quaternion Normalize : aerolibutil/Quaternion Normalize
  singleV1 : Subsystem
  singleV2 : Subsystem
  singleV3 : Subsystem
  vec_rot : Outport
  wires:
  singleV2/1(V2) -> Mux1/2
  singleV3/1(V3) -> Mux1/3
  Mux1/1 -> vec_rot/1
  Quaternion Normalize/1 -> singleV2/1(q), singleV3/1(q), singleV1/1(q)
  vec/1 -> singleV2/2(vec), singleV3/2(vec), singleV1/2(vec)
  singleV1/1(V1) -> Mux1/1
  q/1 -> Quaternion Normalize/1

== system tasks100Hz/calcDeltaE/stdRadianLimit ==
  degrees : Inport
  Bias : Bias  Bias=- 360e7
  Bias1 : Bias  Bias=360e7
  Compare To Constant : simulink/Logic and Bit Operations/Compare To Constant  relop=>=  const=180e7  OutDataTypeStr=boolean
  Compare To Constant1 : simulink/Logic and Bit Operations/Compare To Constant  relop=<  const=-180e7  OutDataTypeStr=boolean
  Switch : Switch  Criteria=u2 > Threshold
  Switch1 : Switch  Criteria=u2 > Threshold
  stdDegrees : Outport
  wires:
  Switch/1 -> stdDegrees/1
  degrees/1 -> Bias/1, Compare To Constant/1, Bias1/1, Compare To Constant1/1, Switch1/3
  Switch1/1 -> Switch/3
  Compare To Constant1/1 -> Switch1/2
  Bias1/1 -> Switch1/1
  Bias/1 -> Switch/1
  Compare To Constant/1 -> Switch/2

== system tasks100Hz/rotationCorrection/Rotation Angles to Quaternions Rotation Order: ZYX ==
  "R1, R2, R3" : Inport
  1/2 : Gain  Gain=0.5  SaturateOnIntegerOverflow=on  OutDataTypeStr=Inherit: Same as input  ParamDataTypeStr=Inherit: Same as input
  Mux4 : Mux
  Selector : Selector  IndexMode=Zero-based  InputPortWidth=3  Indices=0
  Trigonometric Function : Trigonometry
  Trigonometric Function1 : Trigonometry  Operator=cos
  q1 : Constant  Value=0  OutDataTypeStr=single
  q2 : Constant  Value=0  OutDataTypeStr=single
  q : Outport
  wires:
  Selector/1 -> 1/2/1
  "R1, R2, R3"/1 -> Selector/1
  q1/1 -> Mux4/2
  Trigonometric Function1/1 -> Mux4/1
  1/2/1 -> Trigonometric Function/1, Trigonometric Function1/1
  q2/1 -> Mux4/3
  Trigonometric Function/1 -> Mux4/4
  Mux4/1 -> q/1

== system tasks100Hz/rotationCorrection/stdRadianLimit ==
  radians : Inport
  Bias : Bias  Bias=- 2*pi
  Bias1 : Bias  Bias=2*pi
  Compare To Constant : simulink/Logic and Bit Operations/Compare To Constant  relop=>=  const=pi  OutDataTypeStr=boolean
  Compare To Constant1 : simulink/Logic and Bit Operations/Compare To Constant  relop=<  const=-pi  OutDataTypeStr=boolean
  Switch : Switch  Criteria=u2 > Threshold
  Switch1 : Switch  Criteria=u2 > Threshold
  stdRadians : Outport
  wires:
  Switch/1 -> stdRadians/1
  radians/1 -> Bias/1, Compare To Constant/1, Bias1/1, Compare To Constant1/1, Switch1/3
  Switch1/1 -> Switch/3
  Compare To Constant1/1 -> Switch1/2
  Bias1/1 -> Switch1/1
  Bias/1 -> Switch/1
  Compare To Constant/1 -> Switch/2

== system tasks100Hz/accelRotation/Quaternion Rotation/singleV1 ==
  q : Inport
  vec : Inport  Port=2
  Constant1 : Constant  Value=0.5  OutDataTypeStr=single
  Demux1 : Demux
  Demux2 : Demux  Outputs=3
  Demux3 : Demux
  Demux4 : Demux
  Gain : Gain  Gain=2
  Gain1 : Gain  Gain=2
  Gain2 : Gain  Gain=2
  Product{2..10} (9 alike) : Product  RndMeth=Zero
  Sum4 : Sum  Inputs=3
  Sum5 : Sum  Inputs=+|+
  Sum6 : Sum  Inputs=-+|
  Sum7 : Sum  Inputs=--+
  Terminator1 : Terminator
  Terminator2 : Terminator
  V1 : Outport
  wires:
  Demux4/3 -> Product8/2, Product8/1
  Demux4/4 -> Product9/1, Product9/2
  Demux4/1 -> Terminator1/1
  Sum7/1 -> Gain2/1
  Product4/1 -> Sum6/1
  Constant1/1 -> Sum7/3
  Demux2/1 -> Product10/1
  Sum6/1 -> Gain1/1
  Demux2/2 -> Product6/2
  Demux3/1 -> Product4/1
  Product5/1 -> Sum6/2
  Gain2/1 -> Product10/2
  Demux3/3 -> Product4/2
  Demux3/4 -> Product5/2
  Product8/1 -> Sum7/1
  Product9/1 -> Sum7/2
  Demux1/2 -> Product2/1
  Gain/1 -> Product6/1
  Demux4/2 -> Terminator2/1
  Product10/1 -> Sum4/1
  Demux3/2 -> Product5/1
  Demux2/3 -> Product7/2
  Product7/1 -> Sum4/3
  Sum5/1 -> Gain/1
  Demux1/1 -> Product3/1
  Demux1/4 -> Product3/2
  Demux1/3 -> Product2/2
  vec/1 -> Demux2/1
  q/1 -> Demux1/1, Demux4/1, Demux3/1
  Sum4/1 -> V1/1
  Product2/1 -> Sum5/1
  Product6/1 -> Sum4/2
  Product3/1 -> Sum5/2
  Gain1/1 -> Product7/1

== system tasks100Hz/accelRotation/Quaternion Rotation/singleV2 ==
  q : Inport
  vec : Inport  Port=2
  Constant1 : Constant  Value=0.5  OutDataTypeStr=single
  Demux1 : Demux
  Demux2 : Demux  Outputs=3
  Demux3 : Demux
  Demux4 : Demux
  Gain : Gain  Gain=2
  Gain1 : Gain  Gain=2
  Gain2 : Gain  Gain=2
  Product{2..10} (9 alike) : Product  RndMeth=Zero
  Sum4 : Sum  Inputs=3
  Sum5 : Sum  Inputs=+|-
  Sum6 : Sum  Inputs=++|
  Sum7 : Sum  Inputs=--+
  Terminator1 : Terminator
  Terminator2 : Terminator
  V2 : Outport
  wires:
  Product9/1 -> Sum7/2
  Product6/1 -> Sum4/1
  Gain2/1 -> Product10/1
  Product4/1 -> Sum6/1
  Demux4/3 -> Terminator2/1
  Demux2/2 -> Product10/2
  Demux2/1 -> Product6/1
  Demux2/3 -> Product7/2
  Product3/1 -> Sum5/2
  Product2/1 -> Sum5/1
  vec/1 -> Demux2/1
  q/1 -> Demux4/1, Demux3/1, Demux1/1
  Demux1/2 -> Product2/1
  Gain1/1 -> Product7/1
  Demux3/2 -> Product4/2
  Demux3/3 -> Product5/1
  Demux3/4 -> Product5/2
  Demux4/4 -> Product9/2, Product9/1
  Sum6/1 -> Gain1/1
  Demux3/1 -> Product4/1
  Sum4/1 -> V2/1
  Demux4/1 -> Terminator1/1
  Product7/1 -> Sum4/3
  Product8/1 -> Sum7/1
  Constant1/1 -> Sum7/3
  Product10/1 -> Sum4/2
  Demux1/3 -> Product2/2
  Demux4/2 -> Product8/1, Product8/2
  Product5/1 -> Sum6/2
  Sum7/1 -> Gain2/1
  Sum5/1 -> Gain/1
  Gain/1 -> Product6/2
  Demux1/4 -> Product3/2
  Demux1/1 -> Product3/1

== system tasks100Hz/accelRotation/Quaternion Rotation/singleV3 ==
  q : Inport
  vec : Inport  Port=2
  Constant1 : Constant  Value=0.5  OutDataTypeStr=single
  Demux1 : Demux
  Demux2 : Demux  Outputs=3
  Demux3 : Demux
  Demux4 : Demux
  Gain : Gain  Gain=2
  Gain1 : Gain  Gain=2
  Gain2 : Gain  Gain=2
  Product{2..10} (9 alike) : Product  RndMeth=Zero
  Sum4 : Sum  Inputs=3
  Sum5 : Sum  Inputs=+|+
  Sum6 : Sum  Inputs=-+|
  Sum7 : Sum  Inputs=--+
  Terminator : Terminator
  Terminator1 : Terminator
  V3 : Outport
  wires:
  Demux2/3 -> Product10/2
  Constant1/1 -> Sum7/3
  Demux4/1 -> Terminator1/1
  Demux4/4 -> Terminator/1
  Gain2/1 -> Product10/1
  Sum7/1 -> Gain2/1
  Product9/1 -> Sum7/2
  Product8/1 -> Sum7/1
  Demux4/3 -> Product9/1, Product9/2
  Demux4/2 -> Product8/2, Product8/1
  Product6/1 -> Sum4/1
  Product7/1 -> Sum4/2
  Demux2/2 -> Product7/2
  Gain1/1 -> Product7/1
  Demux3/4 -> Product5/2
  Demux3/3 -> Product5/1
  Demux3/2 -> Product4/2
  Demux3/1 -> Product4/1
  Sum6/1 -> Gain1/1
  Product4/1 -> Sum6/1
  Product5/1 -> Sum6/2
  Demux2/1 -> Product6/1
  Gain/1 -> Product6/2
  Sum5/1 -> Gain/1
  Demux1/3 -> Product3/2
  Demux1/1 -> Product3/1
  Demux1/2 -> Product2/1
  Demux1/4 -> Product2/2
  q/1 -> Demux1/1, Demux3/1, Demux4/1
  vec/1 -> Demux2/1
  Product2/1 -> Sum5/1
  Product3/1 -> Sum5/2
  Sum4/1 -> V3/1
  Product10/1 -> Sum4/3
